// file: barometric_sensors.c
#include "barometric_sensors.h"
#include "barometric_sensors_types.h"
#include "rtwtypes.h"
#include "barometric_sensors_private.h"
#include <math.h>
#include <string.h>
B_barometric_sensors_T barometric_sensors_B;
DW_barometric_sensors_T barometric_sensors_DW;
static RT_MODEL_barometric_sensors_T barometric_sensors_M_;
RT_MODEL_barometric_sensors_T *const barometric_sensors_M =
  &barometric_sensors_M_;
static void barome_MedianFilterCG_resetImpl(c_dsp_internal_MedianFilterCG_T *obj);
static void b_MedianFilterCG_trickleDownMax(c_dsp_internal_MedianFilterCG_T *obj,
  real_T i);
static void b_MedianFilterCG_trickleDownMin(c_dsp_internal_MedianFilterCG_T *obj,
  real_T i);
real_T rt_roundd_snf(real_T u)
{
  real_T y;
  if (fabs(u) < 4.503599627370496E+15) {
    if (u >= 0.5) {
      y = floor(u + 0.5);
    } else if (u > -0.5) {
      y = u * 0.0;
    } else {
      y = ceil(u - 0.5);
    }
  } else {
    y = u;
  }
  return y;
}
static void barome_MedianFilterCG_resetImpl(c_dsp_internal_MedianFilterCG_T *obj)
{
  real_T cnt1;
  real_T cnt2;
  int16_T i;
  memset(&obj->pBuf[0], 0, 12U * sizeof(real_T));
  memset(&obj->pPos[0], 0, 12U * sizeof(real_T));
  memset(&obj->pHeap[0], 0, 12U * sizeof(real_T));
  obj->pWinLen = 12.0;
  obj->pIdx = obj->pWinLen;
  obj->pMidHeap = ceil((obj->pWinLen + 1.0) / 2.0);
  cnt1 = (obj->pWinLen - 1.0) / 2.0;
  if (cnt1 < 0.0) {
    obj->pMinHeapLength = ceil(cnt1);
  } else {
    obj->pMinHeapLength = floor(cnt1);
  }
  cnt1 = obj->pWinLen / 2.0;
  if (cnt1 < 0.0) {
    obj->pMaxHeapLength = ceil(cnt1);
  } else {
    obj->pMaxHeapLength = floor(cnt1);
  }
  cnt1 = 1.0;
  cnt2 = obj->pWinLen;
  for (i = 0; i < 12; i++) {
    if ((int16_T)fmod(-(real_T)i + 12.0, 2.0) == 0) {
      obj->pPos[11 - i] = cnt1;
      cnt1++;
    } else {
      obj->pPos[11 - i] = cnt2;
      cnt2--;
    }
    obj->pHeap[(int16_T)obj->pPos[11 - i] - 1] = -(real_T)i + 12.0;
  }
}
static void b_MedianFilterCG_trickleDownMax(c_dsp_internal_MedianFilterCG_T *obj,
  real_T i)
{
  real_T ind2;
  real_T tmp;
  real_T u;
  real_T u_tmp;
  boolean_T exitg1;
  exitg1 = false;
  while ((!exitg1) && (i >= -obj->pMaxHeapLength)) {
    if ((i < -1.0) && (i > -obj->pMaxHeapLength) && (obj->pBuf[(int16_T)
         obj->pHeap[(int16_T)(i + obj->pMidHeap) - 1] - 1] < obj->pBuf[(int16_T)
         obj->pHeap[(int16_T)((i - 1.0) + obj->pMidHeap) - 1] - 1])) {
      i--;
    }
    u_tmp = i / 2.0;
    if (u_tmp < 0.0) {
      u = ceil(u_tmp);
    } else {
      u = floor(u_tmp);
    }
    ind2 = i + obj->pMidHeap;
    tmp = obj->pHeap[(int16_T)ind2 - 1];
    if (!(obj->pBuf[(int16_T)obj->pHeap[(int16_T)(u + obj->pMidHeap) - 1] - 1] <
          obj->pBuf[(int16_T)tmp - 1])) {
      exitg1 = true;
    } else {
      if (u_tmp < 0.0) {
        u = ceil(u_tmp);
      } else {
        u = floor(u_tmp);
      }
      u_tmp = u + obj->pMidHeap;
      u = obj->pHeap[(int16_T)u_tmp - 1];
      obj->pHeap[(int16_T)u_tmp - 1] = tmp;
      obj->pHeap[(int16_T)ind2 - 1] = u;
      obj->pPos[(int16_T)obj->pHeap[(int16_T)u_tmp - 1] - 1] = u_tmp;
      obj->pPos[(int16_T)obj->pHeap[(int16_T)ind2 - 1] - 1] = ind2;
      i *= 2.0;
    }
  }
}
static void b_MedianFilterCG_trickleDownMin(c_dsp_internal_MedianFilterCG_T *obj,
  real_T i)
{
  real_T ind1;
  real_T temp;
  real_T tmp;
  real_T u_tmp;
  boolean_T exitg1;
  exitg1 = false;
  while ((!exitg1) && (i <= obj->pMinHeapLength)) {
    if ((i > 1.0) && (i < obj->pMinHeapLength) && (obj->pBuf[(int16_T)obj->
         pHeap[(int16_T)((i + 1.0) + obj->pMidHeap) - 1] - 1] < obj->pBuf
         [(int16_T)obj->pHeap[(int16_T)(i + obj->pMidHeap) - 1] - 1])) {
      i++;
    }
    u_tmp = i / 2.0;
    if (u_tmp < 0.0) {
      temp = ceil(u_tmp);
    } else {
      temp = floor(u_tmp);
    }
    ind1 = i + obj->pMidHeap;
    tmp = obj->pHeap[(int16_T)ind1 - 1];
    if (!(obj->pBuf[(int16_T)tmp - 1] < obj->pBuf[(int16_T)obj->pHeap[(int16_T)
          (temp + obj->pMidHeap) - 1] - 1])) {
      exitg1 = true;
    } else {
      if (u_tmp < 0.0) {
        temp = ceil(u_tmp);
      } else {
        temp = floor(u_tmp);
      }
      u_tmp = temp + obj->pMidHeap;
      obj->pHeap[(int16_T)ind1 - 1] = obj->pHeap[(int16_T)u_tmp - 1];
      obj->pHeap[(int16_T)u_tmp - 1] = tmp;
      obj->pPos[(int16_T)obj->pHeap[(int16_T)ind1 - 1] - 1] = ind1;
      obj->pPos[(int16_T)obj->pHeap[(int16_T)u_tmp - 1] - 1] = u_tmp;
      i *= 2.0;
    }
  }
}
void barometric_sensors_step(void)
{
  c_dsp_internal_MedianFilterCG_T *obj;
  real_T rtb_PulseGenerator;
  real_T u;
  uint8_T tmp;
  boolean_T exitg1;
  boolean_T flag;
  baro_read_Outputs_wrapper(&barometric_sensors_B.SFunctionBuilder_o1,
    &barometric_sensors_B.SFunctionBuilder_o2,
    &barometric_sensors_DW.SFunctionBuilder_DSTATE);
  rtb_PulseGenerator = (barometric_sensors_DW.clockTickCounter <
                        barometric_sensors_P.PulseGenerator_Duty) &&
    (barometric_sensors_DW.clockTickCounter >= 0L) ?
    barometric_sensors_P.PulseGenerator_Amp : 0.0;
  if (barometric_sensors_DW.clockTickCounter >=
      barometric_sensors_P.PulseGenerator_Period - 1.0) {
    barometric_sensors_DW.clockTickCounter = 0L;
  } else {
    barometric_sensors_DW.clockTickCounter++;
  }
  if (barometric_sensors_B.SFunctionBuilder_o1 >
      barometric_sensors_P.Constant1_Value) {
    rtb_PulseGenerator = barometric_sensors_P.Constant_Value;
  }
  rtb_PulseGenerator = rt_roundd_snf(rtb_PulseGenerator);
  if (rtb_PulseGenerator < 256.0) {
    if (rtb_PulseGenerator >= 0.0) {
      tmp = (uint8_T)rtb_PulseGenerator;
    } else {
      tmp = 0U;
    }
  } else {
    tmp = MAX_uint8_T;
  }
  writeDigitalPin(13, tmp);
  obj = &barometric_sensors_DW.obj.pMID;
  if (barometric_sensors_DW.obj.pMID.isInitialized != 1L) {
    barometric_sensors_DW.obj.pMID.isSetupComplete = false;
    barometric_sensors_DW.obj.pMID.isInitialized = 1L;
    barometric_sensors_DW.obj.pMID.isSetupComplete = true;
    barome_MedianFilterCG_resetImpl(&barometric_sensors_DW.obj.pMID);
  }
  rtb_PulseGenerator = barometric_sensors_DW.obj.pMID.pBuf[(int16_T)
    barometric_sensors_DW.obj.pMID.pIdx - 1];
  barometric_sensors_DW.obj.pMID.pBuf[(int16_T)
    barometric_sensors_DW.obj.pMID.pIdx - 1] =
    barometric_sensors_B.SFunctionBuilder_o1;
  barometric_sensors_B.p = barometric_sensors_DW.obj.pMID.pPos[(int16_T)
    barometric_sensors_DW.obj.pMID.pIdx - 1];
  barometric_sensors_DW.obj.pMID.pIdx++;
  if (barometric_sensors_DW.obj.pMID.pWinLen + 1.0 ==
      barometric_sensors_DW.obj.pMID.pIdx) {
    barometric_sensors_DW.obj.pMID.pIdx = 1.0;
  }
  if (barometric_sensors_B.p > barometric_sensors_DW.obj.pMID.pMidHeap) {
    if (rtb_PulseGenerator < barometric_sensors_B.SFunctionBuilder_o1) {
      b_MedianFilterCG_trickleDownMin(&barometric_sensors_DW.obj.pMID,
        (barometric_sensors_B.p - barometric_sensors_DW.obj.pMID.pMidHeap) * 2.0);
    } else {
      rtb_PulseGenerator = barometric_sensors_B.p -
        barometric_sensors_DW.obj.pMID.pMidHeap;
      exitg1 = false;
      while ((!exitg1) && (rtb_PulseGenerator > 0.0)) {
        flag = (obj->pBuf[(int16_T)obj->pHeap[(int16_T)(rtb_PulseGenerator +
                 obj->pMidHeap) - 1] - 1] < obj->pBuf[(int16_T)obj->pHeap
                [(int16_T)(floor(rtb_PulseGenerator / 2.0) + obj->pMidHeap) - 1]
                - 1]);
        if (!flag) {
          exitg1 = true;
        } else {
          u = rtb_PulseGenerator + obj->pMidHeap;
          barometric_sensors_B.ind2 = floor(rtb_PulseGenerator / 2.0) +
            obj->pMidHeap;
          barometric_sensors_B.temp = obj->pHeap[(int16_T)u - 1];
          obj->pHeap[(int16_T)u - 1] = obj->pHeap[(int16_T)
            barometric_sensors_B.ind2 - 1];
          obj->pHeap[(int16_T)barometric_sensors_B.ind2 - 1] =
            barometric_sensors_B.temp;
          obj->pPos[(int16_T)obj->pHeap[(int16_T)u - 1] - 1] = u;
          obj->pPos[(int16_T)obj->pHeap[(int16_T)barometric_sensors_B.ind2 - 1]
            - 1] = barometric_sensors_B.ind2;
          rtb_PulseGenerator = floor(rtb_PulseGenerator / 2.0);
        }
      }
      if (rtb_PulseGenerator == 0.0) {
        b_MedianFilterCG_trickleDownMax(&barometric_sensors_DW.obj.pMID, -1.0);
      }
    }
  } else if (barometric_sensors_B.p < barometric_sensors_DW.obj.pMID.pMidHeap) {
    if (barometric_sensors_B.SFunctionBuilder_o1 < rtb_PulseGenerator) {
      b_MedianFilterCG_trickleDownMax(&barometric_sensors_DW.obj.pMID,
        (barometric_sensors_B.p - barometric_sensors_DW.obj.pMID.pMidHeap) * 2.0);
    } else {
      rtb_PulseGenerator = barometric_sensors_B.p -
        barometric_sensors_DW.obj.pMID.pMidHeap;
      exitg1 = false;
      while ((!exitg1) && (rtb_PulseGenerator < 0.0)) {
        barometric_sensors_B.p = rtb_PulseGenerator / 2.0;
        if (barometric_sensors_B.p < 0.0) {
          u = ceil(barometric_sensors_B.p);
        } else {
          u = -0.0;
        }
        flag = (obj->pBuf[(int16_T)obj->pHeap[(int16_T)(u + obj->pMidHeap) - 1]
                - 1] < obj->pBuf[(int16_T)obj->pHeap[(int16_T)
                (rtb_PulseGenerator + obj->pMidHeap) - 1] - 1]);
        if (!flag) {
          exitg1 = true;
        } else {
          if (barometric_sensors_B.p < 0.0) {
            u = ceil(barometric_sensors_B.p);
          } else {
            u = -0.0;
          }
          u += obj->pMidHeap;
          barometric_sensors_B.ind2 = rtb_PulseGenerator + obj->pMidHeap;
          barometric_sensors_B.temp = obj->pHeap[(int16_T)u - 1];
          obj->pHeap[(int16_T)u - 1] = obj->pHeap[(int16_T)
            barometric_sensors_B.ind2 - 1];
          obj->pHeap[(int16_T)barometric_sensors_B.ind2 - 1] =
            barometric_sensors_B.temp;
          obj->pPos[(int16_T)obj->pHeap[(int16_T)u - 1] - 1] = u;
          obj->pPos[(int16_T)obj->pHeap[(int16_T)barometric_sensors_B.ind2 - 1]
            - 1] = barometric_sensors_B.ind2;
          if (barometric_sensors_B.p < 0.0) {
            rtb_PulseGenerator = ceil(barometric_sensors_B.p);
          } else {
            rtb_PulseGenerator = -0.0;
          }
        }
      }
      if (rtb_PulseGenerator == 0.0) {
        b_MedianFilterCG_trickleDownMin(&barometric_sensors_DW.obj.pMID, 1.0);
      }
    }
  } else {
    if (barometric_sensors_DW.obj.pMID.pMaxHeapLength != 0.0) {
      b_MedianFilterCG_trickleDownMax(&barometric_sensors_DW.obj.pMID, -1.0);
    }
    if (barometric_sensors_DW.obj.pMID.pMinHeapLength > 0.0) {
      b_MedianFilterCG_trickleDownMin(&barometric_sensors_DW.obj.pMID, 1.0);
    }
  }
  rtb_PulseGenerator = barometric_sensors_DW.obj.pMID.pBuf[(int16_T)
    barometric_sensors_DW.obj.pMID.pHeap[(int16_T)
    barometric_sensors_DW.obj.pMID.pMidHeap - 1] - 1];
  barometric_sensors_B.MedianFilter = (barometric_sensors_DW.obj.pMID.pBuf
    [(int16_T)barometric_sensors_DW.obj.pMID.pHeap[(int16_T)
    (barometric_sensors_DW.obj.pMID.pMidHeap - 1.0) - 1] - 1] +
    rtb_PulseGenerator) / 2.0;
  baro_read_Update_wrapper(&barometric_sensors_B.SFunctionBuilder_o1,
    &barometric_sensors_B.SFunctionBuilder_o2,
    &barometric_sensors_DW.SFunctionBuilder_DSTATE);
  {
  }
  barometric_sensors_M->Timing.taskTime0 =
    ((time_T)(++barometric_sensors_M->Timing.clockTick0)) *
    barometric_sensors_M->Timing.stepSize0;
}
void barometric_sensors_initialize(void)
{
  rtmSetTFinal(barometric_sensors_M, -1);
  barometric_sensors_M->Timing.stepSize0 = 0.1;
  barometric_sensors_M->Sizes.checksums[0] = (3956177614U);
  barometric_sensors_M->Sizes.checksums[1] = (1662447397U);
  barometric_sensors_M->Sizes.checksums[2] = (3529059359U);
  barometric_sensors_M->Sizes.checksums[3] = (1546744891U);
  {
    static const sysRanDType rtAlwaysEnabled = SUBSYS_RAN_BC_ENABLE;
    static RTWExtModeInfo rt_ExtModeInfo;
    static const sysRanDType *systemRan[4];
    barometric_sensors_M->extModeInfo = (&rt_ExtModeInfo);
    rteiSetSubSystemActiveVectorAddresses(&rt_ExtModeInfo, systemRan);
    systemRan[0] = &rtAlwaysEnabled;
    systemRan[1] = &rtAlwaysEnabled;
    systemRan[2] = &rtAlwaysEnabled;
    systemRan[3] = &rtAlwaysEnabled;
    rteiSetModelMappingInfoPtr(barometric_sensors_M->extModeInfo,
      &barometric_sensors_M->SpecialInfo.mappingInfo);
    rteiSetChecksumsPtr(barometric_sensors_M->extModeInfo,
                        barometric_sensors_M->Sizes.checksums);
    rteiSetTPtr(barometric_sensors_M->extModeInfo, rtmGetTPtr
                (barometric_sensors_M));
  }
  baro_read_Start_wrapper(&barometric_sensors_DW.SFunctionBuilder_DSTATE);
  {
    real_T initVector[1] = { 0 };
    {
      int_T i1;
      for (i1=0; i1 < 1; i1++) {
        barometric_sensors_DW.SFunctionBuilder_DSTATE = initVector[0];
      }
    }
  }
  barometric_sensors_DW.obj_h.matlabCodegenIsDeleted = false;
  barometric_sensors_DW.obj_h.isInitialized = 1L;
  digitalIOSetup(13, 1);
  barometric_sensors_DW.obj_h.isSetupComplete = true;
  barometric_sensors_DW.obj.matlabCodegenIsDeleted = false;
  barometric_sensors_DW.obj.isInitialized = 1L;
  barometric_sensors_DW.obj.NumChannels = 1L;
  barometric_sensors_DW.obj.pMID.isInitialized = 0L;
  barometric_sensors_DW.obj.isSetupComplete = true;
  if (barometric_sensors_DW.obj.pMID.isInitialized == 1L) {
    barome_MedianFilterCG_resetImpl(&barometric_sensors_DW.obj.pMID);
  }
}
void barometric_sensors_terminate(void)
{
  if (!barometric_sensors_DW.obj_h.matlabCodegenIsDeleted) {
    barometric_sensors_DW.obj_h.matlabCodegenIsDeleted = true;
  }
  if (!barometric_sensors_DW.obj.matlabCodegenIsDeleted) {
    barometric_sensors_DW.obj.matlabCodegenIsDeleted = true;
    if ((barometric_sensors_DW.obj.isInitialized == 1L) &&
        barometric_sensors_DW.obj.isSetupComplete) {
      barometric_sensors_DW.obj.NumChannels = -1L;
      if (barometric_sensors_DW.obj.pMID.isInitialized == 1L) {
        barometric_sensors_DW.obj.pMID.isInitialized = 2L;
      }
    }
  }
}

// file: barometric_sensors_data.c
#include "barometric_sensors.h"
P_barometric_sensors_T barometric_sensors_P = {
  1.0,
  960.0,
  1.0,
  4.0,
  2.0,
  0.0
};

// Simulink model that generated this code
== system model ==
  DigitalOutput#1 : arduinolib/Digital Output  pinNumber=13  <- 1: Switch#1
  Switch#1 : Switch  Criteria=u2 > Threshold  <- 1: Constant, 2: RelationalOperator#1, 3: PulseGenerator
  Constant : Constant
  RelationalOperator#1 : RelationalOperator  Operator=>  <- 1: SFunctionBuilder, 2: Constant1
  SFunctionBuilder : S-Function  FunctionName=baro_read
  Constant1 : Constant  Value=960
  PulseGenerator : DiscretePulseGenerator  Period=4  PulseWidth=2
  MedianFilter : dspstat3/Median Filter  <- 1: SFunctionBuilder
